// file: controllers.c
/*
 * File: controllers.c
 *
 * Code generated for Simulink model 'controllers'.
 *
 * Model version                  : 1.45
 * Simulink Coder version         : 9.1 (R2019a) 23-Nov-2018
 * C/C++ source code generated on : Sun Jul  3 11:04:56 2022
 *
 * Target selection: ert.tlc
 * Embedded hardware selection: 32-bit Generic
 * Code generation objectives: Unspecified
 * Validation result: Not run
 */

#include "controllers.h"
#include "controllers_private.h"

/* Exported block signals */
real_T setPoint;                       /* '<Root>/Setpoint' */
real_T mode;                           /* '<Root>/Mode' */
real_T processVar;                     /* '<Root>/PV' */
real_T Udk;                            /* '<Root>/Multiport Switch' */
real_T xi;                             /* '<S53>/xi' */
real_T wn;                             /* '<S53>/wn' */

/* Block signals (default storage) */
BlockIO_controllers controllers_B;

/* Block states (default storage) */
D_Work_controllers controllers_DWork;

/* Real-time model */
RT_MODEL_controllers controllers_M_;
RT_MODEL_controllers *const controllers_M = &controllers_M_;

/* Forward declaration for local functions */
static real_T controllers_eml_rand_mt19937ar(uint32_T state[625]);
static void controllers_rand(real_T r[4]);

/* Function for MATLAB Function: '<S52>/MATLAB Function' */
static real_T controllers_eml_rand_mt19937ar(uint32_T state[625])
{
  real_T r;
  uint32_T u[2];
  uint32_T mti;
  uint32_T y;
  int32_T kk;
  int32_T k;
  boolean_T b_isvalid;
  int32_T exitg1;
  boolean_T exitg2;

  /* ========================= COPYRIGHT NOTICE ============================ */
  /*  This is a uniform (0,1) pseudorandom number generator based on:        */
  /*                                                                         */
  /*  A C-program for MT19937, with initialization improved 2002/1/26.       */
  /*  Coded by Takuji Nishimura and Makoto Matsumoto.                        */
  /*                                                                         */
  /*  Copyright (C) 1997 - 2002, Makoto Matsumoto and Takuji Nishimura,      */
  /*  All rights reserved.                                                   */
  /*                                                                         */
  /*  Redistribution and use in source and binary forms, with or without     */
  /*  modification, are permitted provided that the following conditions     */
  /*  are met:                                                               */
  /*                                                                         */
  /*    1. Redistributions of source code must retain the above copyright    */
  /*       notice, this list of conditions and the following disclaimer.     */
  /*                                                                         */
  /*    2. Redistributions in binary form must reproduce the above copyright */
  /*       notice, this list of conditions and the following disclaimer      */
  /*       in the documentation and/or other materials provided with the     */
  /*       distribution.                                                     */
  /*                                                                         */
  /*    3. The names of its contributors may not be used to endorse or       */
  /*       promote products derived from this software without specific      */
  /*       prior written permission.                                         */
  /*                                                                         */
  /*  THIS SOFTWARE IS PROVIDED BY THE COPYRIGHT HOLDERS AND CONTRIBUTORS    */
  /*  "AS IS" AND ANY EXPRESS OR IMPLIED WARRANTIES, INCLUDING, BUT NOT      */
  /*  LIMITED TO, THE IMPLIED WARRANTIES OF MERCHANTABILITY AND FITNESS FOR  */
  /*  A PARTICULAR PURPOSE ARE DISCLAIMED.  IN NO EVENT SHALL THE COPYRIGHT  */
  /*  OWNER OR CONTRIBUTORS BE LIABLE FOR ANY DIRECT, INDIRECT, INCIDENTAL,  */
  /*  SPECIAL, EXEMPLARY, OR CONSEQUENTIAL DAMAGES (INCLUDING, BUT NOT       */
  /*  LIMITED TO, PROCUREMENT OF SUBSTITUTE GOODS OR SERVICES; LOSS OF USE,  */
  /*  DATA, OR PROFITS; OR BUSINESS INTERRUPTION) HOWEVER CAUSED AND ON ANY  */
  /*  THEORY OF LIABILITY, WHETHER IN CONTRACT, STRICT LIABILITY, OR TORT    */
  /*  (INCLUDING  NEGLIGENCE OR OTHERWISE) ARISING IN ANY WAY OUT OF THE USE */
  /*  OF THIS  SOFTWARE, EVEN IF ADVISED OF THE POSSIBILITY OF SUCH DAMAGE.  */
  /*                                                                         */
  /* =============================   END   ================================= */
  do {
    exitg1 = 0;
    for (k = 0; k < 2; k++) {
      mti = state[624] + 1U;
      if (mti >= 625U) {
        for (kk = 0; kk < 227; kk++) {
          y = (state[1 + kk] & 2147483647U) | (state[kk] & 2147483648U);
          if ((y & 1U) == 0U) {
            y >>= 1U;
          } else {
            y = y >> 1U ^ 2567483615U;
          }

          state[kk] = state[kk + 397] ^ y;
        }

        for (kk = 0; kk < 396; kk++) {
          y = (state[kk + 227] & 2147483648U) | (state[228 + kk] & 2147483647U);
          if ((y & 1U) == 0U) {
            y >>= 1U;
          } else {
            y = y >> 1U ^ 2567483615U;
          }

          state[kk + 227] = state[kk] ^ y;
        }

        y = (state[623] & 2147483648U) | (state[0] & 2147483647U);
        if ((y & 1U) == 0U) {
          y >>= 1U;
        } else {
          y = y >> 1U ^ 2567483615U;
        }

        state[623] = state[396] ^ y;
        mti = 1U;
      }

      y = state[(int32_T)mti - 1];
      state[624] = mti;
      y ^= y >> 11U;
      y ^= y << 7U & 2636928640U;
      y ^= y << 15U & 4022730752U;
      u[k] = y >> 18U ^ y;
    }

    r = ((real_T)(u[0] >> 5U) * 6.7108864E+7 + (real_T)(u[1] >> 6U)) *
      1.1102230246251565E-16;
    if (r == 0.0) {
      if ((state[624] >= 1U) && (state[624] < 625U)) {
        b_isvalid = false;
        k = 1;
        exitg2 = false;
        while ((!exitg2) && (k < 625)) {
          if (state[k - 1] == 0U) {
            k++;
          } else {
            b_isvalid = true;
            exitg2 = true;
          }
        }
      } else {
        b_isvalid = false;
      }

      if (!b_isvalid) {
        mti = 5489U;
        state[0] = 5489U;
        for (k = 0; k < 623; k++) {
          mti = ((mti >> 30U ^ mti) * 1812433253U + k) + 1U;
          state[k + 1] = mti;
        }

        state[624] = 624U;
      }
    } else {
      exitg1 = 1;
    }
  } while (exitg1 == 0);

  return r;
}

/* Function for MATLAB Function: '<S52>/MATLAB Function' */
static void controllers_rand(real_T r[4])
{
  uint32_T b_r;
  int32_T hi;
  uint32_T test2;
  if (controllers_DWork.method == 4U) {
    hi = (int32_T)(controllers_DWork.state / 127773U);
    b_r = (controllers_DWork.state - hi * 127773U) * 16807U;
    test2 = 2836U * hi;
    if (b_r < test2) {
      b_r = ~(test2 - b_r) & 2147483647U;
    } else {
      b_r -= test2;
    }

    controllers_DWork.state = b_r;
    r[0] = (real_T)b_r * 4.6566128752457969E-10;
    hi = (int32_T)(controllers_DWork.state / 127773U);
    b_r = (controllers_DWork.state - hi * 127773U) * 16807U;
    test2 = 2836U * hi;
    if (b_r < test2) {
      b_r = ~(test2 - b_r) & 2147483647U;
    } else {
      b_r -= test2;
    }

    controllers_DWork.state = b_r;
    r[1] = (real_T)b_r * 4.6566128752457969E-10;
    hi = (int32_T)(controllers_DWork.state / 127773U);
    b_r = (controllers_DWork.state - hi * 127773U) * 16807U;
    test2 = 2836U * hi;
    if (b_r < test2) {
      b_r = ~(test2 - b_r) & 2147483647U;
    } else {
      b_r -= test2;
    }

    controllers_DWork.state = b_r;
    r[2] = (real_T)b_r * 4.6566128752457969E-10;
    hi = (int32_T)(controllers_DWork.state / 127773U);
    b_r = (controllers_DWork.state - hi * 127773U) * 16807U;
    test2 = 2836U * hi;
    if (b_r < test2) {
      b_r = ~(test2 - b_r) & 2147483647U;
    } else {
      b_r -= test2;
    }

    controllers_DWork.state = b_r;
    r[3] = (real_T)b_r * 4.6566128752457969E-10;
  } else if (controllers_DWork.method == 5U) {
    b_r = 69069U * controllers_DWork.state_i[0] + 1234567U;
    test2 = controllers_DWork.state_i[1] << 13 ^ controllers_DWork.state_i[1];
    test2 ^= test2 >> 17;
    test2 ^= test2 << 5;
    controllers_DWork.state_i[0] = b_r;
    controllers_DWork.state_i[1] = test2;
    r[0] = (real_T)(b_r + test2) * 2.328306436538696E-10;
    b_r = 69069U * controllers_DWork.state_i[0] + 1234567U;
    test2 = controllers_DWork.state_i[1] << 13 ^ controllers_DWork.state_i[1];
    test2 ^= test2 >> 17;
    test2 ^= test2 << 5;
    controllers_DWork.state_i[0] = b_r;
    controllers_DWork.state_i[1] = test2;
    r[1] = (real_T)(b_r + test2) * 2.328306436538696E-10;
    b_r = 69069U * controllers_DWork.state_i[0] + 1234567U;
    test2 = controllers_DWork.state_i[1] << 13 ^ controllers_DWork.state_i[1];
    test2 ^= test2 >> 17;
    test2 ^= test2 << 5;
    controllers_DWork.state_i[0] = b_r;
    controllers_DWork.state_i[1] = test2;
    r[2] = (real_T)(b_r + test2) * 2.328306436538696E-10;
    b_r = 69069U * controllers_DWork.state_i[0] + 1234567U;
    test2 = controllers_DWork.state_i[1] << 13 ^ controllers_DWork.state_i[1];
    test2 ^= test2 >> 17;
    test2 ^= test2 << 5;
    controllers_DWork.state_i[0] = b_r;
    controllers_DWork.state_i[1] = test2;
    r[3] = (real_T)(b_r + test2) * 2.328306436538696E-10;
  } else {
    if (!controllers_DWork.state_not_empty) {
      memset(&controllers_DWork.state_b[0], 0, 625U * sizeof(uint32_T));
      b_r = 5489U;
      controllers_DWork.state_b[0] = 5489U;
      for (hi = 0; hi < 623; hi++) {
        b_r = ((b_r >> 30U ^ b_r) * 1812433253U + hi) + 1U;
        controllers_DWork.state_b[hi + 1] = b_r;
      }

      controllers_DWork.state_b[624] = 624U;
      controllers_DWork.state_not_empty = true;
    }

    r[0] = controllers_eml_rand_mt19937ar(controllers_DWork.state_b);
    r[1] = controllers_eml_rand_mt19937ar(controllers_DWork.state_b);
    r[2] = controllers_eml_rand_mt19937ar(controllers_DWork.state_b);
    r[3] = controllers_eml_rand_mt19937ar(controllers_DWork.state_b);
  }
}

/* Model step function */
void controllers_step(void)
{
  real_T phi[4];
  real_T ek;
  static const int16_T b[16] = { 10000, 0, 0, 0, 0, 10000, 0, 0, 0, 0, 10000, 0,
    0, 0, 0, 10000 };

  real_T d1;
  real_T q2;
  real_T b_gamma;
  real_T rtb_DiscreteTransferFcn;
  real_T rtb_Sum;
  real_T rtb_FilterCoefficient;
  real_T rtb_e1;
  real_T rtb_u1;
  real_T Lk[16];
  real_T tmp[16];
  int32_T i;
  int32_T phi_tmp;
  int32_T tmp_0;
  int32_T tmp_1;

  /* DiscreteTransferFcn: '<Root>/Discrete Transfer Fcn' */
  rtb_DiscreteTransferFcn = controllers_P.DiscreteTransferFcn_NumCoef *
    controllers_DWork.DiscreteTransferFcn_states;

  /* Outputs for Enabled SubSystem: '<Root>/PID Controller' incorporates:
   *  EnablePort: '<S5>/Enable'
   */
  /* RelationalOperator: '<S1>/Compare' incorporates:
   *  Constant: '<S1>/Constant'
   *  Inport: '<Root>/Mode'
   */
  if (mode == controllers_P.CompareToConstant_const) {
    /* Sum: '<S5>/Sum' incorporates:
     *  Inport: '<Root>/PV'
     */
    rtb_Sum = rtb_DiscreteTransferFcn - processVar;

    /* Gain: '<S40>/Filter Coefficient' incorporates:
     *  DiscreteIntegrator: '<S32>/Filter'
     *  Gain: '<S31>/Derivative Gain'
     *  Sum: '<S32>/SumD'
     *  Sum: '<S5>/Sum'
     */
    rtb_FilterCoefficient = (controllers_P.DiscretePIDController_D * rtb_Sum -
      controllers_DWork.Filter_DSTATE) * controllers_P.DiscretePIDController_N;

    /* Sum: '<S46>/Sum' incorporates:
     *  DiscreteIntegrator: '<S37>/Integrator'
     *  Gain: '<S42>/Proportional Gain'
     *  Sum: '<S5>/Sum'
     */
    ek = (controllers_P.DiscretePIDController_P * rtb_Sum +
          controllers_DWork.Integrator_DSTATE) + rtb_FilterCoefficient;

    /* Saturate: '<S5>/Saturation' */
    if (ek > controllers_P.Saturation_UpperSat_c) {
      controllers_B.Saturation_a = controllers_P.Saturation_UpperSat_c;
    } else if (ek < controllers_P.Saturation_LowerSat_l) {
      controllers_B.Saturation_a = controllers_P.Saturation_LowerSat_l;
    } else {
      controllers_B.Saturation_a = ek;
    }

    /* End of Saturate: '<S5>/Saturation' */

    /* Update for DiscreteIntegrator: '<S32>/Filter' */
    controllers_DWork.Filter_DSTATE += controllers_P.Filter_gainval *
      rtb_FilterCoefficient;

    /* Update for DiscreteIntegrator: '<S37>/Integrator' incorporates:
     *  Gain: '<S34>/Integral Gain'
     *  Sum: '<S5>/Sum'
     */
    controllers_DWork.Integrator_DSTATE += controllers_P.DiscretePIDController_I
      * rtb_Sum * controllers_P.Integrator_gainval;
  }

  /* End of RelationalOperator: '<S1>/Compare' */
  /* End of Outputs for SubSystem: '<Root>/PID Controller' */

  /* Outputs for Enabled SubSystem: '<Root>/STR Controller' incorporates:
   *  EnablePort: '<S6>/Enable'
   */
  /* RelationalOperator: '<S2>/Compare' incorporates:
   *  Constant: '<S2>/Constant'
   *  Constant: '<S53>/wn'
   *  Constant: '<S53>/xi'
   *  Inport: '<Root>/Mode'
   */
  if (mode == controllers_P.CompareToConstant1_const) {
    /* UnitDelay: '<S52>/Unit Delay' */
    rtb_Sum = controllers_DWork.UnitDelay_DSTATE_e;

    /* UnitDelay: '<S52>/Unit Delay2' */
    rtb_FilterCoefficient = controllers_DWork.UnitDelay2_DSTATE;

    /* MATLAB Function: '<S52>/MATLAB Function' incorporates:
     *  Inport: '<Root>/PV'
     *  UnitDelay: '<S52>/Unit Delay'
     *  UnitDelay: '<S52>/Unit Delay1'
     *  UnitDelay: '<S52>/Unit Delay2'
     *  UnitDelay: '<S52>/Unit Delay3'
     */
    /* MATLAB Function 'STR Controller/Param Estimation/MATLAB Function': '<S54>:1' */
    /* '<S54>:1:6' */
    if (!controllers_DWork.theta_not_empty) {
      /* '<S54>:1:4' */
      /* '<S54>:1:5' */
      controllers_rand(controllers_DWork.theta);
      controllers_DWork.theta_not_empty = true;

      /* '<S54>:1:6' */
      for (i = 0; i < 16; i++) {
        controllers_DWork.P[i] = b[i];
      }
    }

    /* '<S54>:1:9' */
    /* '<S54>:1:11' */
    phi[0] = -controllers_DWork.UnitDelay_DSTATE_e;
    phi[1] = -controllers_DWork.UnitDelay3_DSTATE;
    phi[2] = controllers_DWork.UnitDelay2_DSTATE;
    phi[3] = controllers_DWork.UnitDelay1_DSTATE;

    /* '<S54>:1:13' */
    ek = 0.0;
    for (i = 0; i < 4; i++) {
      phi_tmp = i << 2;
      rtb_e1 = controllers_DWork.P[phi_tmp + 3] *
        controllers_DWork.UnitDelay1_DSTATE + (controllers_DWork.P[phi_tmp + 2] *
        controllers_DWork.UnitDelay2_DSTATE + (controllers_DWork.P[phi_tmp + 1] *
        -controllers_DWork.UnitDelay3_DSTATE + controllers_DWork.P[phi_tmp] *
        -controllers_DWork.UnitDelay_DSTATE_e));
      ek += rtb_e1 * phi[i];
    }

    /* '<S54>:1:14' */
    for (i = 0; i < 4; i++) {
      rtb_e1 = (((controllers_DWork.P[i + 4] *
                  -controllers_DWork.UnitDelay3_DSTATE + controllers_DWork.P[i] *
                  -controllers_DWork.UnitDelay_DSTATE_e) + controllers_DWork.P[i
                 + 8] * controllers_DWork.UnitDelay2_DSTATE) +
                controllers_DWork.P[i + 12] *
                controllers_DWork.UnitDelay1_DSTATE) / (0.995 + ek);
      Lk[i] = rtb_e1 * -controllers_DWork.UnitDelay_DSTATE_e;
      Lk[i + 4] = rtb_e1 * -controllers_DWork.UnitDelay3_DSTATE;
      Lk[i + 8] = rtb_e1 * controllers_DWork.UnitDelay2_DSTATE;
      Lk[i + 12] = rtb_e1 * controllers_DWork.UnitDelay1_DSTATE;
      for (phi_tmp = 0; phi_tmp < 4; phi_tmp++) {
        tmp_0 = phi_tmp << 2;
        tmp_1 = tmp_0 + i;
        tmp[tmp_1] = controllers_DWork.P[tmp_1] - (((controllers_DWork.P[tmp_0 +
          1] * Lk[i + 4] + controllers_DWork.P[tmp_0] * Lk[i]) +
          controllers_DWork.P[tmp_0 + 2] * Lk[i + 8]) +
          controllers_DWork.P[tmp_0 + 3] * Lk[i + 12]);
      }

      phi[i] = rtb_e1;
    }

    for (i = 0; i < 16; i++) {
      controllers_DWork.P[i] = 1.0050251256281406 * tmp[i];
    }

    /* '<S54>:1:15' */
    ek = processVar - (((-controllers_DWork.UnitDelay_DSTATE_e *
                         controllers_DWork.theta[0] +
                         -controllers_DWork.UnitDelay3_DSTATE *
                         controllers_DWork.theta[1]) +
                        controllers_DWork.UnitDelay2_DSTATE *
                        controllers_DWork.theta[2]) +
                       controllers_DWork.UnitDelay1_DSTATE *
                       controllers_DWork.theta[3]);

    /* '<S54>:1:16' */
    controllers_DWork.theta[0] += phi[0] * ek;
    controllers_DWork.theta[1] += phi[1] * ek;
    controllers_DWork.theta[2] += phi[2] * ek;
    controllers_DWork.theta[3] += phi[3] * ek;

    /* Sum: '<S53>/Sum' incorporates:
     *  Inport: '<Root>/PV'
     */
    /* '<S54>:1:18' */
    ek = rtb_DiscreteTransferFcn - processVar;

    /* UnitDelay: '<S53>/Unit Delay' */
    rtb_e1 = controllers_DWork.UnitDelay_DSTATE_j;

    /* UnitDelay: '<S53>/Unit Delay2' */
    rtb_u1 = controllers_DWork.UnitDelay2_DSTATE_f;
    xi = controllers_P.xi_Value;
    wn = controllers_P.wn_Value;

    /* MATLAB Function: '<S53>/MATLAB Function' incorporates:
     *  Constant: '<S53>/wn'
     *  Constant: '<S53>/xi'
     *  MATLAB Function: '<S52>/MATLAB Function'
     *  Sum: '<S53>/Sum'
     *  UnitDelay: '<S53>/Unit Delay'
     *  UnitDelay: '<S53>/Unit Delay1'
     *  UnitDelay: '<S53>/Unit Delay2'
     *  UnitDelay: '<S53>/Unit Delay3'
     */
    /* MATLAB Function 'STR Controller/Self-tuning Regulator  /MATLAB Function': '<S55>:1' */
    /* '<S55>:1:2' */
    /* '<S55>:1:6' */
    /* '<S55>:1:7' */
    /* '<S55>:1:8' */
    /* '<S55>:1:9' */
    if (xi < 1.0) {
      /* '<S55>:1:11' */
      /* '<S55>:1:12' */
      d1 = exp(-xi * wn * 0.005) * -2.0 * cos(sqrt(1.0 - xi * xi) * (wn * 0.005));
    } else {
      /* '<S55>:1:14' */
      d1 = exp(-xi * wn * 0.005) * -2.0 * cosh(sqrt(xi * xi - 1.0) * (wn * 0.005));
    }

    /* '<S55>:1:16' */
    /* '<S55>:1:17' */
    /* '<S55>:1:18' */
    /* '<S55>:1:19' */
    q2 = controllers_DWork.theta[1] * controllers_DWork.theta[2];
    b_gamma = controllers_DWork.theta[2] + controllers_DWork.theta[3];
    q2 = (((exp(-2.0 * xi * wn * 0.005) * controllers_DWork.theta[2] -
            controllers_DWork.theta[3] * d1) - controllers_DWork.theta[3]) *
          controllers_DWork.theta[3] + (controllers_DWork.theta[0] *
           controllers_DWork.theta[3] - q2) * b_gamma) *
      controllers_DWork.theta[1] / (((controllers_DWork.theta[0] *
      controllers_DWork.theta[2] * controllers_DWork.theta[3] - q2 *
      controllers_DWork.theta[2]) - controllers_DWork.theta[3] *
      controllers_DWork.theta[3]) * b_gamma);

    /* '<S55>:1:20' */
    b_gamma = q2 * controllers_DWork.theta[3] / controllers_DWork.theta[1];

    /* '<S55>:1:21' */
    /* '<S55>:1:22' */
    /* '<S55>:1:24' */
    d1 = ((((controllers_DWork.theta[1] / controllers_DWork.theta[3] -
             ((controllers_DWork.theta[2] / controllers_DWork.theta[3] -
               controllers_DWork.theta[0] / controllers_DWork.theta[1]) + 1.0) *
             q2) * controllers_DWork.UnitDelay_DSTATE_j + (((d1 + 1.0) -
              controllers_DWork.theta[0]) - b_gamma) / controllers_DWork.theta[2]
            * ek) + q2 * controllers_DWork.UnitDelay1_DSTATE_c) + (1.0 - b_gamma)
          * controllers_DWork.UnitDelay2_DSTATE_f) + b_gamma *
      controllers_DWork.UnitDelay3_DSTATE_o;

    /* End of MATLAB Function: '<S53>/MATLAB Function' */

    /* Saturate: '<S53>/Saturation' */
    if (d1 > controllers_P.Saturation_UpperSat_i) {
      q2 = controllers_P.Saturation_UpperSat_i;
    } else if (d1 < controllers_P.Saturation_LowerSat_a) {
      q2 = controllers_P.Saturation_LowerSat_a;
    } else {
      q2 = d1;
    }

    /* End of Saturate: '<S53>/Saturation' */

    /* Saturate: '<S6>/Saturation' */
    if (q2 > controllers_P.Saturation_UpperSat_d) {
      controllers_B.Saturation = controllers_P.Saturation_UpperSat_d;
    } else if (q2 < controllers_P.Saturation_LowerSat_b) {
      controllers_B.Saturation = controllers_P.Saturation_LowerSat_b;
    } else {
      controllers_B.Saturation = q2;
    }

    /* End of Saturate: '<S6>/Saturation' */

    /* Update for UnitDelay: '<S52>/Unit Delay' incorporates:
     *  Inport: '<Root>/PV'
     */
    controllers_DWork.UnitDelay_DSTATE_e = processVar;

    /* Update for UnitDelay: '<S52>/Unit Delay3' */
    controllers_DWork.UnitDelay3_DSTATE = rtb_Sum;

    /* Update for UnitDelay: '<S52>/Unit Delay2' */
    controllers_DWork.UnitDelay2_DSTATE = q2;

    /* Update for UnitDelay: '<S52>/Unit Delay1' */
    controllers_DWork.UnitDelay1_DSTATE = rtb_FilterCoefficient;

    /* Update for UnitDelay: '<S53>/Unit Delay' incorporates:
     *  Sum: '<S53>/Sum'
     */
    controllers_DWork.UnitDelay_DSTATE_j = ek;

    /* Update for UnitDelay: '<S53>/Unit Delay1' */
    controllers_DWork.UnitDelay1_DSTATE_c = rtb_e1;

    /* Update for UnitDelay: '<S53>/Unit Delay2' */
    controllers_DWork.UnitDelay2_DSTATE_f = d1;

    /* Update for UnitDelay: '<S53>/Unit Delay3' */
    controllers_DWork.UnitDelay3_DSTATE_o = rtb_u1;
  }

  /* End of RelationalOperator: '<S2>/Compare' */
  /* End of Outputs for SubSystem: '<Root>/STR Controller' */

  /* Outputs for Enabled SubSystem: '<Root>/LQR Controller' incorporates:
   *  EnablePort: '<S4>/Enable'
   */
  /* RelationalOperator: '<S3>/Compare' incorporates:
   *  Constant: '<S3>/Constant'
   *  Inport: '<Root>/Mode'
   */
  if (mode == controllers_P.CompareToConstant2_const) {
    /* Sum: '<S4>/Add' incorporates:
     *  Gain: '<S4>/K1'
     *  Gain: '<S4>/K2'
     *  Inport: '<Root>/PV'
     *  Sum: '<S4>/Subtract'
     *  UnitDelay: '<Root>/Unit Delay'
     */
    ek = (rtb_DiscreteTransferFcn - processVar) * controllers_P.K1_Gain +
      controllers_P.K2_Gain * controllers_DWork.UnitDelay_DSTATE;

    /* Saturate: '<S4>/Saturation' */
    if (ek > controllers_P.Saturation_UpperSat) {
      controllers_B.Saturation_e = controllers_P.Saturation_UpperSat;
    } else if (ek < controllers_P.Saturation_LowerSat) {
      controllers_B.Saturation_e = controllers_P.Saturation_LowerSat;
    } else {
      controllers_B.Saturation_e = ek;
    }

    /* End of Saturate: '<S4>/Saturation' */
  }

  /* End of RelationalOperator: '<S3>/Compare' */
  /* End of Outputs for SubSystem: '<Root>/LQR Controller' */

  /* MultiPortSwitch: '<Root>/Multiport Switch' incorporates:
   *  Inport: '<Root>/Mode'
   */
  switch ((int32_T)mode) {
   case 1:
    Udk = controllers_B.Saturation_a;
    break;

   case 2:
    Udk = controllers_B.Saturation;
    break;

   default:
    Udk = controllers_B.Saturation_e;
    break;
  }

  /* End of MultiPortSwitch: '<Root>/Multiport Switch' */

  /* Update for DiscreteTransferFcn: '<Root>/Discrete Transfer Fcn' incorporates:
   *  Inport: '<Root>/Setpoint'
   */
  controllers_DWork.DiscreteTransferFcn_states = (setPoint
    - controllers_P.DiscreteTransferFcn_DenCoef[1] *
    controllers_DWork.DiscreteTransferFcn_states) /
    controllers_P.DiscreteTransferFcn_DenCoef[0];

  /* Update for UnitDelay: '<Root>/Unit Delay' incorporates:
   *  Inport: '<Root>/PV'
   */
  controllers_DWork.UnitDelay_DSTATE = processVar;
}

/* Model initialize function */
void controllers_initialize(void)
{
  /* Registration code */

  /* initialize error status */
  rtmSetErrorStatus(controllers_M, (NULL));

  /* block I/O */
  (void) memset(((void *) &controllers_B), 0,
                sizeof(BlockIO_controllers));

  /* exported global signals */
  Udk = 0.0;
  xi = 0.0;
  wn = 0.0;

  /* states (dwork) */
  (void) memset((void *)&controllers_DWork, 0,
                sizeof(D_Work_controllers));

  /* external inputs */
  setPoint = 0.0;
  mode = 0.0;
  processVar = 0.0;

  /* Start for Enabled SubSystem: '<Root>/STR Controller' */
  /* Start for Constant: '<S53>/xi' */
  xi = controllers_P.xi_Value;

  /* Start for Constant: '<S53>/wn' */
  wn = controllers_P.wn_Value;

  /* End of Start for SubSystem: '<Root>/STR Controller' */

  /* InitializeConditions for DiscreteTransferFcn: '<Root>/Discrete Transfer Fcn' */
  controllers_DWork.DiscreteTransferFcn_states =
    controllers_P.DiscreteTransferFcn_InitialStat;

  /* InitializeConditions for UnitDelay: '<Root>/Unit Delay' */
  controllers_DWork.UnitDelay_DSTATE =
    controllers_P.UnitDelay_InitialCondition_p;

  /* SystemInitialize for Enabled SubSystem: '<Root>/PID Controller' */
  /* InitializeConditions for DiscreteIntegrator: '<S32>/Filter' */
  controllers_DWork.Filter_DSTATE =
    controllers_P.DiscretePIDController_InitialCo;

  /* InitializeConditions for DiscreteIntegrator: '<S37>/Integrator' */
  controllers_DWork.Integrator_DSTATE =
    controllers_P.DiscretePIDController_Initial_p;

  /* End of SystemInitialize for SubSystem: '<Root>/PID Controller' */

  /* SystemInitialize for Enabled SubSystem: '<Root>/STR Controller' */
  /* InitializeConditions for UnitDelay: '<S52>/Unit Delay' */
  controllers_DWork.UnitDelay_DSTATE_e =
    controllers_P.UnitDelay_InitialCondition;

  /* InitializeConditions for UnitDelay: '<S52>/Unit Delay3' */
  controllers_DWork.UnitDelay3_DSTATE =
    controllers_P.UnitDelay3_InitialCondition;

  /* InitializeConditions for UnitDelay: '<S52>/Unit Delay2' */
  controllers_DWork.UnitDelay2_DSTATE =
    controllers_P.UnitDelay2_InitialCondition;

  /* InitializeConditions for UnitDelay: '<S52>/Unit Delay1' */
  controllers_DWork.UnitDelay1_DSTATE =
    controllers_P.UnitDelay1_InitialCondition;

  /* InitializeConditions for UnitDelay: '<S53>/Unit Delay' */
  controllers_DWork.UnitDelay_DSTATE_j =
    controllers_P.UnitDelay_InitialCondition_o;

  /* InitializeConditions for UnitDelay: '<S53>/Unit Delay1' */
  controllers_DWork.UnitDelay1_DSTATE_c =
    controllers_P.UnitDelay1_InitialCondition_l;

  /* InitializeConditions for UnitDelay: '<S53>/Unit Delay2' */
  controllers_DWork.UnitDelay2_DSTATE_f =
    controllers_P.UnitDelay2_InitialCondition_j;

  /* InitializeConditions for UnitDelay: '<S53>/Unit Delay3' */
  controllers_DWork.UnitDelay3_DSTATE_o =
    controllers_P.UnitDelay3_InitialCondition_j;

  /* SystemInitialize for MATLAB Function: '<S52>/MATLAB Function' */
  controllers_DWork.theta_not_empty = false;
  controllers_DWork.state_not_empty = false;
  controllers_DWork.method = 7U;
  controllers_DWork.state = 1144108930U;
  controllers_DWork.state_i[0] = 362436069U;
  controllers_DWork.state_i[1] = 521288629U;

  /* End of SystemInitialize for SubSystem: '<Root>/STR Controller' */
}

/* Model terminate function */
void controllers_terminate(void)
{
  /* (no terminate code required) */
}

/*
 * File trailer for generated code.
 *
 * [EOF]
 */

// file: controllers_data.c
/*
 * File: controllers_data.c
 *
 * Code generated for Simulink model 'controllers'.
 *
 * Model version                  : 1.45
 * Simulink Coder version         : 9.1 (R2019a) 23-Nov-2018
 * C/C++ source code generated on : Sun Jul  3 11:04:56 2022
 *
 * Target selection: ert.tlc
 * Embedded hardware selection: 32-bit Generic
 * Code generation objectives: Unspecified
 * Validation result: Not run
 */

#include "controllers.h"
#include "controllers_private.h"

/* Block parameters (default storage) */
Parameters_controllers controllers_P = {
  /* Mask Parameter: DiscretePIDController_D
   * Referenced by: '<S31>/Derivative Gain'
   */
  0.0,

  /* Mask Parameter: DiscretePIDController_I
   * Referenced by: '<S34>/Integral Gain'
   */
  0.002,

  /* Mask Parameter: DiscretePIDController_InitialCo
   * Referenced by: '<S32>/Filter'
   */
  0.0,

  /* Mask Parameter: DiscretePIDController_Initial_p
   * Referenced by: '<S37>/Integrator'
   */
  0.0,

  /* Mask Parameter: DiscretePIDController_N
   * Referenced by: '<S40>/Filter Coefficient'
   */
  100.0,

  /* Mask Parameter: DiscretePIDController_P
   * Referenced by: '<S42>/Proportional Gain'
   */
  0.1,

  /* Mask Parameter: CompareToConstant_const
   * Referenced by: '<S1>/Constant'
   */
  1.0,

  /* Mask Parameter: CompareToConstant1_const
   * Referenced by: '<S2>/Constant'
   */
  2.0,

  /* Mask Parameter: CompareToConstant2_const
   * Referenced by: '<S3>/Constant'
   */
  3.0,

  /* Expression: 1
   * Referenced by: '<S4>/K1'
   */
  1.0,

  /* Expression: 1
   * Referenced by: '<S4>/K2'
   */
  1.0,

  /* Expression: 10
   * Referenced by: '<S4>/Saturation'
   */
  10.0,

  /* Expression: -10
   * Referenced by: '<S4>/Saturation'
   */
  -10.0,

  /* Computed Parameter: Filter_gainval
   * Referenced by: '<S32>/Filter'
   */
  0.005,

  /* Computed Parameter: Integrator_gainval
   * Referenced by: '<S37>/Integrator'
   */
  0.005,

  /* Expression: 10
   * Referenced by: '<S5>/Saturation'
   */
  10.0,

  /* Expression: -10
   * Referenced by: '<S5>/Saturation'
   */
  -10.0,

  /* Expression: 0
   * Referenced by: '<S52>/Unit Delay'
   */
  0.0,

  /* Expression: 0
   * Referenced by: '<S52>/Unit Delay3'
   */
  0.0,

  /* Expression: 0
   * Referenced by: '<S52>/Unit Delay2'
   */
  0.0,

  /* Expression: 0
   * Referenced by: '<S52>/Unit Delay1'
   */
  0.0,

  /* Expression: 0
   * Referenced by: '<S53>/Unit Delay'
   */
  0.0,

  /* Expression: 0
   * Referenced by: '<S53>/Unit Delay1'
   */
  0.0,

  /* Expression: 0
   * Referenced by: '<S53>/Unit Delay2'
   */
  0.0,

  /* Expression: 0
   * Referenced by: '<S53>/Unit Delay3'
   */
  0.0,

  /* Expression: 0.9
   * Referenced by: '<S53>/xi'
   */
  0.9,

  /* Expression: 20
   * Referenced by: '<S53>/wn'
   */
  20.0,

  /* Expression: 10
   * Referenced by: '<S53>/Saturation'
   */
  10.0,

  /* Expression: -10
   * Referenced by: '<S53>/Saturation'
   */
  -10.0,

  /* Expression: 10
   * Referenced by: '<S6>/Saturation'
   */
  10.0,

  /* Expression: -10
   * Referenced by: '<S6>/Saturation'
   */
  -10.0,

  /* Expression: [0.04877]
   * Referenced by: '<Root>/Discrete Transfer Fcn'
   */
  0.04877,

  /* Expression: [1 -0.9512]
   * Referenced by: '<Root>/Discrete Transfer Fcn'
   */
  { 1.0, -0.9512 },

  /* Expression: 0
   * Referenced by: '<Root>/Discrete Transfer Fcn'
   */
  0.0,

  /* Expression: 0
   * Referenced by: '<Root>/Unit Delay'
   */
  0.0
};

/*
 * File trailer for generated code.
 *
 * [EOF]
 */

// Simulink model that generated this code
simulink model "controllers"  (Simulink 9.3)
settings: Solver=FixedStepDiscrete  StartTime=0.0  StopTime=10.0  FixedStep=0.005  RelTol=1e-3  EnableMultiTasking=on
libraries: simulink x4

== system controllers ==
  note: Volts
  Setpoint : Inport
  Mode : Inport  Port=2
  PV : Inport  Port=3
  Compare To Constant : simulink/Logic and Bit Operations/Compare To Constant  relop===  const=1  OutDataTypeStr=boolean
  Compare To Constant1 : simulink/Logic and Bit Operations/Compare To Constant  relop===  const=2  OutDataTypeStr=boolean
  Compare To Constant2 : simulink/Logic and Bit Operations/Compare To Constant  relop===  const=3  OutDataTypeStr=boolean
  Discrete Transfer Fcn : DiscreteTransferFcn  Numerator=[0.04877]  Denominator=[1 -0.9512]
  LQR Controller : Subsystem
  Multiport Switch : MultiPortSwitch
  PID Controller : Subsystem
  STR Controller : Subsystem
  Unit Delay : UnitDelay  SampleTime=-1  HasFrameUpgradeWarning=on
  Udk : Outport
  wires:
  LQR Controller/1(Udk) -> Multiport Switch/4
  Compare To Constant2/1 -> LQR Controller/Enable
  Unit Delay/1 -> LQR Controller/3(dPV)
  Mode/1 -> Multiport Switch/1, Compare To Constant/1, Compare To Constant1/1, Compare To Constant2/1  "mode"
  STR Controller/1(Udk) -> Multiport Switch/3
  PID Controller/1(Udk) -> Multiport Switch/2
  PV/1 -> Unit Delay/1, LQR Controller/2(PV), STR Controller/2(PV), PID Controller/2(PV)  "processVar"
  Compare To Constant/1 -> PID Controller/Enable  "enable"
  Multiport Switch/1 -> Udk/1  "Udk"
  Setpoint/1 -> Discrete Transfer Fcn/1  "setPoint"
  Compare To Constant1/1 -> STR Controller/Enable
  Discrete Transfer Fcn/1 -> LQR Controller/1(Setpoint), STR Controller/1(SP), PID Controller/1(SP)

== system controllers/LQR Controller ==
  Setpoint : Inport
  PV : Inport  Port=2
  dPV : Inport  Port=3
  Enable : EnablePort
  Add : Sum
  K1 : Gain
  K2 : Gain
  Saturation : Saturate  UpperLimit=10  LowerLimit=-10
  Subtract : Sum  Inputs=+-
  Udk : Outport
  wires:
  Setpoint/1 -> Subtract/1
  PV/1 -> Subtract/2
  Saturation/1 -> Udk/1
  Add/1 -> Saturation/1
  K1/1 -> Add/1
  K2/1 -> Add/2
  Subtract/1 -> K1/1
  dPV/1 -> K2/1

== system controllers/PID Controller ==
  SP : Inport
  PV : Inport  Port=2
  Enable : EnablePort
  Discrete PID Controller : simulink/Continuous/PID Controller  Controller=PID  Form=Parallel  TimeDomain=Discrete-time  SampleTime=-1  IntegratorMethod=Forward Euler  FilterMethod=Forward Euler  ControllerParametersSource=internal  P=0.1  I=0.002  D=0  UseFilter=on  N=100  TunerSelectOption=Transfer Function Based (PID Tuner App)  InitialConditionSource=internal  InitialConditionForIntegrator=0  InitialConditionForFilter=0  DifferentiatorICPrevScaledInput=0  ExternalReset=none  TrackingMode=off  Kt=1  LimitOutput=off  UpperSaturationLimit=inf  LowerSaturationLimit=-inf  LinearizeAsGain=off  AntiWindupMode=none  Kb=1  POutMin=[]  POutMax=[]  IOutMin=[]  IOutMax=[]  DOutMin=[]  DOutMax=[]  NOutMin=[]  NOutMax=[]  SumOutMin=[]  SumOutMax=[]  SaturationOutMin=[]  SaturationOutMax=[]  PParamMin=[]  PParamMax=[]  IParamMin=[]  IParamMax=[]  DParamMin=[]  DParamMax=[]  NParamMin=[]  NParamMax=[]  KbParamMin=[]  KbParamMax=[]  KtParamMin=[]  KtParamMax=[]  KbOutMin=[]  KbOutMax=[]  KtOutMin=[]  KtOutMax=[]  IntegratorOutMin=[]  IntegratorOutMax=[]  FilterOutMin=[]  FilterOutMax=[]  SumI1OutMin=[]  SumI1OutMax=[]  SumI2OutMin=[]  SumI2OutMax=[]  SumI3OutMin=[]  SumI3OutMax=[]  SumI4OutMin=[]  SumI4OutMax=[]  SumDOutMin=[]  SumDOutMax=[]  DifferentiatorOutMin=[]  DifferentiatorOutMax=[]  FilterDiffOutCoefMin=[]  FilterDiffOutCoefMax=[]  ReciprocalOutMin=[]  ReciprocalOutMax=[]  SumDenOutMin=[]  SumDenOutMax=[]  SumNumOutMin=[]  SumNumOutMax=[]  DivideOutMin=[]  DivideOutMax=[]  IntegratorContinuousStateAttributes=''  IntegratorStateMustResolveToSignalObject=off  IntegratorRTWStateStorageClass=Auto  FilterContinuousStateAttributes=''  FilterStateMustResolveToSignalObject=off  FilterRTWStateStorageClass=Auto  ParallelPVariant=InternalParameters  IdealPVariant=Disabled  IVariant=InternalParameters  DVariant=InternalParameters  IntegratorVariant=Discrete  SatVariant=Disabled  AWVariant=Passthrough  PCopyVariant=Disabled  TRVariant=Disabled  FdbkBlocksVariant=Forward  IdealPFdbkVariant=Disabled  SatFdbkVariant=Disabled  DerivativeFilterVariant=ForwardEulerFilter  NVariant=InternalParameters  NCopyVariant=Disabled  FilterICVariant=InternalICsFilter  IntegratorICVariant=InternalICs  ExternalResetVariant=Disabled  TRSumVariant=Passthrough  SumFdbkVariant=Disabled  SumVariant=Sum_PID
  Saturation : Saturate  UpperLimit=10  LowerLimit=-10
  Sum : Sum  Inputs=|+-
  Udk : Outport
  wires:
  SP/1 -> Sum/1
  PV/1 -> Sum/2
  Sum/1 -> Discrete PID Controller/1
  Discrete PID Controller/1 -> Saturation/1
  Saturation/1 -> Udk/1

== system controllers/STR Controller ==
  SP : Inport
  PV : Inport  Port=2
  Enable : EnablePort
  Param Estimation : Subsystem
  Saturation : Saturate  UpperLimit=10  LowerLimit=-10
  "Self-tuning Regulator  " : Subsystem
  Udk : Outport
  wires:
  PV/1 -> "Self-tuning Regulator  "/3(y), Param Estimation/1("y ")  "y"
  "Self-tuning Regulator  "/1(udk) -> Param Estimation/2(u), Saturation/1  "u"
  SP/1 -> "Self-tuning Regulator  "/2(Setpoint)
  Param Estimation/1(theta) -> "Self-tuning Regulator  "/1(theta)
  Saturation/1 -> Udk/1

== system controllers/STR Controller/Param Estimation ==
  "y " : Inport  PortDimensions=1
  u : Inport  Port=2  PortDimensions=1
  MATLAB Function : MATLAB Function  TreatAsAtomicUnit=on
  Unit Delay{,1..3} (4 alike) : UnitDelay  SampleTime=-1  HasFrameUpgradeWarning=on
  theta : Outport  PortDimensions=4
  wires:
  "y "/1 -> MATLAB Function/1(yk), Unit Delay/1
  u/1 -> Unit Delay2/1
  MATLAB Function/1(theta_out) -> theta/1
  Unit Delay/1 -> Unit Delay3/1, MATLAB Function/2(yk_1)
  Unit Delay2/1 -> MATLAB Function/4(uk_1), Unit Delay1/1
  Unit Delay3/1 -> MATLAB Function/3(yk_2)
  Unit Delay1/1 -> MATLAB Function/5(uk_2)

== system controllers/STR Controller/Self-tuning Regulator   ==
  note: Right Click -> Block Params -> Signal Attributes -> Rewrite Port dimensions
  note: theta = [a1 a2 b1 b2]'
  theta : Inport  PortDimensions=4
  Setpoint : Inport  Port=2  PortDimensions=1
  y : Inport  Port=3  PortDimensions=1
  MATLAB Function : MATLAB Function  TreatAsAtomicUnit=on
  Saturation : Saturate  UpperLimit=10  LowerLimit=-10
  Sum : Sum  Inputs=|+-
  Unit Delay{,1..3} (4 alike) : UnitDelay  SampleTime=-1  HasFrameUpgradeWarning=on
  wn : Constant  Value=20
  xi : Constant  Value=0.9
  udk : Outport  PortDimensions=1
  wires:
  Saturation/1 -> udk/1
  Setpoint/1 -> Sum/1
  y/1 -> Sum/2
  Sum/1 -> MATLAB Function/2(e), Unit Delay/1  "e"
  Unit Delay/1 -> MATLAB Function/3(e1), Unit Delay1/1  "e1"
  theta/1 -> MATLAB Function/1(theta)
  Unit Delay1/1 -> MATLAB Function/4(e2)  "e2"
  MATLAB Function/1(u) -> Saturation/1, Unit Delay2/1
  Unit Delay2/1 -> MATLAB Function/5(u1), Unit Delay3/1  "u1"
  Unit Delay3/1 -> MATLAB Function/6(u2)  "u2"
  xi/1 -> MATLAB Function/7(xi)  "xi"
  wn/1 -> MATLAB Function/8(wn)  "wn"

== matlab function STR Controller/Self-tuning Regulator /MATLAB Function ==
function u = STR(theta,e,e1,e2,u1,u2,xi,wn)
T0 = 0.005;
%xi = 0.98
%wn = 20;
% Gan lai thong so de thuan tien viec tinh toan
a1 = theta(1);
a2 = theta(2);
b1 = theta(3);
b2 = theta(4);
% Tinh thong so bo dieu khien
if(xi<1)
d1 = -2*exp(-xi*wn*T0)*cos(wn*T0*sqrt(1-xi^2)); % xi<1
else
d1 = -2*exp(-xi*wn*T0)*cosh(wn*T0*sqrt(xi^2-1)); % xi>1
end
d2 = exp(-2*xi*wn*T0);
r1 = (b1+b2)*(a1*b1*b2-a2*b1*b1-b2*b2);
s1 = a2*((b1+b2)*(a1*b2-a2*b1)+b2*(b1*d2-b2*d1-b2));
q2 = s1/r1;
gamma = q2*b2/a2;
q1 = a2/b2-q2*(b1/b2-a1/a2+1);
q0 = (d1+1-a1-gamma)/b1;
% Luat dieu khien
u = q0*e + q1*e1 + q2*e2 + (1-gamma)*u1+ gamma*u2;

== matlab function STR Controller/Param Estimation/MATLAB Function ==
function theta_out = fcn(yk,yk_1,yk_2,uk_1,uk_2)
persistent theta P

if (isempty(theta))
    theta = rand(4,1);
    P = 10000*eye(4);
end

lambda = 0.995;

phi = [-yk_1;-yk_2;uk_1;uk_2];

Lk = P*phi/(lambda + phi'*P*phi);
P = 1/lambda*(P-Lk*phi'*P);
ek = yk - phi'*theta;
theta = theta + Lk*ek;

theta_out = theta;
end
